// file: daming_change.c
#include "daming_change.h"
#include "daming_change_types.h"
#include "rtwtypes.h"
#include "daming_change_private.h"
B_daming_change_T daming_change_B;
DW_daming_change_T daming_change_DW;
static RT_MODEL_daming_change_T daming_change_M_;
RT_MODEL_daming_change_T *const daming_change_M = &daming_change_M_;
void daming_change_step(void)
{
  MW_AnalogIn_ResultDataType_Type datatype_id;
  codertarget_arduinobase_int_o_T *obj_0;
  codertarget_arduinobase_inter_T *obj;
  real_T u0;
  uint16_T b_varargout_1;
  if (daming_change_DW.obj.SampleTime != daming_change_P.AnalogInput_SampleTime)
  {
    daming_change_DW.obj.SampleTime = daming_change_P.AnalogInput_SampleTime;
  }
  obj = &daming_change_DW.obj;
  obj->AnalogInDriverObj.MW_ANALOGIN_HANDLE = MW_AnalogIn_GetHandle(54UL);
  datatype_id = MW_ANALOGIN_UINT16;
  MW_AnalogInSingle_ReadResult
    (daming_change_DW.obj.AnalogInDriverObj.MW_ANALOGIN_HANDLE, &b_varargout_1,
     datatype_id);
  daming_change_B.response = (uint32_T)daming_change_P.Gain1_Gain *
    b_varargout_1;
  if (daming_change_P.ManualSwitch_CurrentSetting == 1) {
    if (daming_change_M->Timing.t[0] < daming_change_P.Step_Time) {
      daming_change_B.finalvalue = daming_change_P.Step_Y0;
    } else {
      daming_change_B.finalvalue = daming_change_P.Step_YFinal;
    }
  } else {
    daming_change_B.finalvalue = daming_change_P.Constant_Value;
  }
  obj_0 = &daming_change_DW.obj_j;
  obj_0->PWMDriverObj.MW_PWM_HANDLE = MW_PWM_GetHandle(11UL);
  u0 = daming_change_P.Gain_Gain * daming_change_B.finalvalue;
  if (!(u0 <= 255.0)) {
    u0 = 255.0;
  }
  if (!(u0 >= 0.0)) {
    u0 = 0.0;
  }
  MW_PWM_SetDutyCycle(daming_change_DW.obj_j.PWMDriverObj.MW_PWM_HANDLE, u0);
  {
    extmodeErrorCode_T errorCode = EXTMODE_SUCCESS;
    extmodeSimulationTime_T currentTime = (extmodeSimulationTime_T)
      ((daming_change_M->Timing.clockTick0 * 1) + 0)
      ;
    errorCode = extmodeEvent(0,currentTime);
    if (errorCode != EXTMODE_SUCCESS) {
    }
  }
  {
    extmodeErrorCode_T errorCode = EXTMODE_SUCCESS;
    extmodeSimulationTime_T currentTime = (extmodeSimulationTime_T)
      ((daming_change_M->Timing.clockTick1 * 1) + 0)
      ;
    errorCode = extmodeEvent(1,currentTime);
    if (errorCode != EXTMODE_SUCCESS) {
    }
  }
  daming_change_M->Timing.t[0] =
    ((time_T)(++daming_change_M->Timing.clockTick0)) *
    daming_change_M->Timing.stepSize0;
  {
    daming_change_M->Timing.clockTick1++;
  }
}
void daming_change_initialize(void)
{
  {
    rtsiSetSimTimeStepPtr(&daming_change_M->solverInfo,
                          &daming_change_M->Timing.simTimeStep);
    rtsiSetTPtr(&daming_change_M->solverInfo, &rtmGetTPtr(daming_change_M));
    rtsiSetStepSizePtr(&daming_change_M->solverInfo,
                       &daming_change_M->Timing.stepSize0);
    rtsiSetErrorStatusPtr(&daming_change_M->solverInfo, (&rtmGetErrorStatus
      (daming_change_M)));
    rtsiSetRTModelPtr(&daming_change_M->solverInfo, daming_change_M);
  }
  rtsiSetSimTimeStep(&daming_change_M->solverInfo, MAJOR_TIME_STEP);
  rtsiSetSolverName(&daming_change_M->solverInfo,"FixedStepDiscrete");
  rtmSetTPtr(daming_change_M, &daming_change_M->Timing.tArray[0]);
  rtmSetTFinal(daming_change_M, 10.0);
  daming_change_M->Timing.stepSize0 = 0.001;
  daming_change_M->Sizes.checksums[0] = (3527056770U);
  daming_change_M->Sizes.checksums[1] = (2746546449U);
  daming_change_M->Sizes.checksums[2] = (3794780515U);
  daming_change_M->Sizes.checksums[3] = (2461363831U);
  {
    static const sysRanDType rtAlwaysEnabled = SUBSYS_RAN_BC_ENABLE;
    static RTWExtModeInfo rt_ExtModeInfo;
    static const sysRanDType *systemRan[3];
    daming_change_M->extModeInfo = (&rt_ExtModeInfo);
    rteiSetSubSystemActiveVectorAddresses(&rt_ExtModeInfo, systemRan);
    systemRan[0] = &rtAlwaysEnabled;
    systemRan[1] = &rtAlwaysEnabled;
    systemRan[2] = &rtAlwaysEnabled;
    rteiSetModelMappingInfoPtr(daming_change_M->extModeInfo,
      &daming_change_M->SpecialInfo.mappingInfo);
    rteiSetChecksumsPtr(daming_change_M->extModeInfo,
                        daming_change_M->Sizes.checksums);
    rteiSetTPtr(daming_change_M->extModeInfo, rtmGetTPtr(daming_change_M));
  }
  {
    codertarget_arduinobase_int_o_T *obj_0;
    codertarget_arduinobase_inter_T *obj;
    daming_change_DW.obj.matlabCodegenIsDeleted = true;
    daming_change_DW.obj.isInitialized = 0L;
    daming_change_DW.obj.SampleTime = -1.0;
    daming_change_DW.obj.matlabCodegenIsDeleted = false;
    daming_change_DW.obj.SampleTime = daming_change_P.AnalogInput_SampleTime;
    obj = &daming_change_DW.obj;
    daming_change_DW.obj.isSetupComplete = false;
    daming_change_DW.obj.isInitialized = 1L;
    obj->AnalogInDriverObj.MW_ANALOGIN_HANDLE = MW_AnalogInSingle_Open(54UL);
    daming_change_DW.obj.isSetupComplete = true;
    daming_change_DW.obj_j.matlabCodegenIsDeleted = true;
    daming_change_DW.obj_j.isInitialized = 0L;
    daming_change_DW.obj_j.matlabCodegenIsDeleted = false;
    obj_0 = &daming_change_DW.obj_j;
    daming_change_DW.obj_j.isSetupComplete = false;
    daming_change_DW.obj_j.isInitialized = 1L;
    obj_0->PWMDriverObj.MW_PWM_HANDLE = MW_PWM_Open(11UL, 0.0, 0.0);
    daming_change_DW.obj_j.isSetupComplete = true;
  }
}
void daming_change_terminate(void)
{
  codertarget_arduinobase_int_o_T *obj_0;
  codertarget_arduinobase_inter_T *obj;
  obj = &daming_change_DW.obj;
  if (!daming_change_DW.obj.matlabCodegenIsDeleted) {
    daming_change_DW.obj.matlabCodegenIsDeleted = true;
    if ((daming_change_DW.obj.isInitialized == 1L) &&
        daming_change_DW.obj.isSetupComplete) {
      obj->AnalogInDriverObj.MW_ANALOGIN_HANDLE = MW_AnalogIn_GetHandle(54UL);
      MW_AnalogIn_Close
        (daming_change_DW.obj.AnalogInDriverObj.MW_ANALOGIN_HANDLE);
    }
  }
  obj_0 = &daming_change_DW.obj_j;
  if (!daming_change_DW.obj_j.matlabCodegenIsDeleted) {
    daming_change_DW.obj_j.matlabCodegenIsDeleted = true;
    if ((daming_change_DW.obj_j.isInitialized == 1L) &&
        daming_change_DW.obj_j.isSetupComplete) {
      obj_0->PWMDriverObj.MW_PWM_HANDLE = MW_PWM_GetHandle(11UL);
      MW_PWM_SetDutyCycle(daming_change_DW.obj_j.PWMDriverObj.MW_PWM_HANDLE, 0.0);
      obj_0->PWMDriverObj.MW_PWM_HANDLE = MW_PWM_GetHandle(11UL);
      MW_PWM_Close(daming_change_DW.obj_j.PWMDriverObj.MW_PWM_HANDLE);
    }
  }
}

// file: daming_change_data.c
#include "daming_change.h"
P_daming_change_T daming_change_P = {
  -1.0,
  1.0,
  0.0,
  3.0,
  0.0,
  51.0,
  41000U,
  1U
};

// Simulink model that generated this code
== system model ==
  Gain1 : Gain  Gain=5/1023  <- 1: AnalogInput
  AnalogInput : arduinolib/Analog Input  pinNumber=0
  PWM : arduinolib/PWM  pinNumber=11  <- 1: Gain
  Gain : Gain  Gain=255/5  <- 1: ManualSwitch
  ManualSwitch : ManualSwitch  <- 1: Step, 2: Constant
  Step : Step  After=3
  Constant : Constant  Value=0
